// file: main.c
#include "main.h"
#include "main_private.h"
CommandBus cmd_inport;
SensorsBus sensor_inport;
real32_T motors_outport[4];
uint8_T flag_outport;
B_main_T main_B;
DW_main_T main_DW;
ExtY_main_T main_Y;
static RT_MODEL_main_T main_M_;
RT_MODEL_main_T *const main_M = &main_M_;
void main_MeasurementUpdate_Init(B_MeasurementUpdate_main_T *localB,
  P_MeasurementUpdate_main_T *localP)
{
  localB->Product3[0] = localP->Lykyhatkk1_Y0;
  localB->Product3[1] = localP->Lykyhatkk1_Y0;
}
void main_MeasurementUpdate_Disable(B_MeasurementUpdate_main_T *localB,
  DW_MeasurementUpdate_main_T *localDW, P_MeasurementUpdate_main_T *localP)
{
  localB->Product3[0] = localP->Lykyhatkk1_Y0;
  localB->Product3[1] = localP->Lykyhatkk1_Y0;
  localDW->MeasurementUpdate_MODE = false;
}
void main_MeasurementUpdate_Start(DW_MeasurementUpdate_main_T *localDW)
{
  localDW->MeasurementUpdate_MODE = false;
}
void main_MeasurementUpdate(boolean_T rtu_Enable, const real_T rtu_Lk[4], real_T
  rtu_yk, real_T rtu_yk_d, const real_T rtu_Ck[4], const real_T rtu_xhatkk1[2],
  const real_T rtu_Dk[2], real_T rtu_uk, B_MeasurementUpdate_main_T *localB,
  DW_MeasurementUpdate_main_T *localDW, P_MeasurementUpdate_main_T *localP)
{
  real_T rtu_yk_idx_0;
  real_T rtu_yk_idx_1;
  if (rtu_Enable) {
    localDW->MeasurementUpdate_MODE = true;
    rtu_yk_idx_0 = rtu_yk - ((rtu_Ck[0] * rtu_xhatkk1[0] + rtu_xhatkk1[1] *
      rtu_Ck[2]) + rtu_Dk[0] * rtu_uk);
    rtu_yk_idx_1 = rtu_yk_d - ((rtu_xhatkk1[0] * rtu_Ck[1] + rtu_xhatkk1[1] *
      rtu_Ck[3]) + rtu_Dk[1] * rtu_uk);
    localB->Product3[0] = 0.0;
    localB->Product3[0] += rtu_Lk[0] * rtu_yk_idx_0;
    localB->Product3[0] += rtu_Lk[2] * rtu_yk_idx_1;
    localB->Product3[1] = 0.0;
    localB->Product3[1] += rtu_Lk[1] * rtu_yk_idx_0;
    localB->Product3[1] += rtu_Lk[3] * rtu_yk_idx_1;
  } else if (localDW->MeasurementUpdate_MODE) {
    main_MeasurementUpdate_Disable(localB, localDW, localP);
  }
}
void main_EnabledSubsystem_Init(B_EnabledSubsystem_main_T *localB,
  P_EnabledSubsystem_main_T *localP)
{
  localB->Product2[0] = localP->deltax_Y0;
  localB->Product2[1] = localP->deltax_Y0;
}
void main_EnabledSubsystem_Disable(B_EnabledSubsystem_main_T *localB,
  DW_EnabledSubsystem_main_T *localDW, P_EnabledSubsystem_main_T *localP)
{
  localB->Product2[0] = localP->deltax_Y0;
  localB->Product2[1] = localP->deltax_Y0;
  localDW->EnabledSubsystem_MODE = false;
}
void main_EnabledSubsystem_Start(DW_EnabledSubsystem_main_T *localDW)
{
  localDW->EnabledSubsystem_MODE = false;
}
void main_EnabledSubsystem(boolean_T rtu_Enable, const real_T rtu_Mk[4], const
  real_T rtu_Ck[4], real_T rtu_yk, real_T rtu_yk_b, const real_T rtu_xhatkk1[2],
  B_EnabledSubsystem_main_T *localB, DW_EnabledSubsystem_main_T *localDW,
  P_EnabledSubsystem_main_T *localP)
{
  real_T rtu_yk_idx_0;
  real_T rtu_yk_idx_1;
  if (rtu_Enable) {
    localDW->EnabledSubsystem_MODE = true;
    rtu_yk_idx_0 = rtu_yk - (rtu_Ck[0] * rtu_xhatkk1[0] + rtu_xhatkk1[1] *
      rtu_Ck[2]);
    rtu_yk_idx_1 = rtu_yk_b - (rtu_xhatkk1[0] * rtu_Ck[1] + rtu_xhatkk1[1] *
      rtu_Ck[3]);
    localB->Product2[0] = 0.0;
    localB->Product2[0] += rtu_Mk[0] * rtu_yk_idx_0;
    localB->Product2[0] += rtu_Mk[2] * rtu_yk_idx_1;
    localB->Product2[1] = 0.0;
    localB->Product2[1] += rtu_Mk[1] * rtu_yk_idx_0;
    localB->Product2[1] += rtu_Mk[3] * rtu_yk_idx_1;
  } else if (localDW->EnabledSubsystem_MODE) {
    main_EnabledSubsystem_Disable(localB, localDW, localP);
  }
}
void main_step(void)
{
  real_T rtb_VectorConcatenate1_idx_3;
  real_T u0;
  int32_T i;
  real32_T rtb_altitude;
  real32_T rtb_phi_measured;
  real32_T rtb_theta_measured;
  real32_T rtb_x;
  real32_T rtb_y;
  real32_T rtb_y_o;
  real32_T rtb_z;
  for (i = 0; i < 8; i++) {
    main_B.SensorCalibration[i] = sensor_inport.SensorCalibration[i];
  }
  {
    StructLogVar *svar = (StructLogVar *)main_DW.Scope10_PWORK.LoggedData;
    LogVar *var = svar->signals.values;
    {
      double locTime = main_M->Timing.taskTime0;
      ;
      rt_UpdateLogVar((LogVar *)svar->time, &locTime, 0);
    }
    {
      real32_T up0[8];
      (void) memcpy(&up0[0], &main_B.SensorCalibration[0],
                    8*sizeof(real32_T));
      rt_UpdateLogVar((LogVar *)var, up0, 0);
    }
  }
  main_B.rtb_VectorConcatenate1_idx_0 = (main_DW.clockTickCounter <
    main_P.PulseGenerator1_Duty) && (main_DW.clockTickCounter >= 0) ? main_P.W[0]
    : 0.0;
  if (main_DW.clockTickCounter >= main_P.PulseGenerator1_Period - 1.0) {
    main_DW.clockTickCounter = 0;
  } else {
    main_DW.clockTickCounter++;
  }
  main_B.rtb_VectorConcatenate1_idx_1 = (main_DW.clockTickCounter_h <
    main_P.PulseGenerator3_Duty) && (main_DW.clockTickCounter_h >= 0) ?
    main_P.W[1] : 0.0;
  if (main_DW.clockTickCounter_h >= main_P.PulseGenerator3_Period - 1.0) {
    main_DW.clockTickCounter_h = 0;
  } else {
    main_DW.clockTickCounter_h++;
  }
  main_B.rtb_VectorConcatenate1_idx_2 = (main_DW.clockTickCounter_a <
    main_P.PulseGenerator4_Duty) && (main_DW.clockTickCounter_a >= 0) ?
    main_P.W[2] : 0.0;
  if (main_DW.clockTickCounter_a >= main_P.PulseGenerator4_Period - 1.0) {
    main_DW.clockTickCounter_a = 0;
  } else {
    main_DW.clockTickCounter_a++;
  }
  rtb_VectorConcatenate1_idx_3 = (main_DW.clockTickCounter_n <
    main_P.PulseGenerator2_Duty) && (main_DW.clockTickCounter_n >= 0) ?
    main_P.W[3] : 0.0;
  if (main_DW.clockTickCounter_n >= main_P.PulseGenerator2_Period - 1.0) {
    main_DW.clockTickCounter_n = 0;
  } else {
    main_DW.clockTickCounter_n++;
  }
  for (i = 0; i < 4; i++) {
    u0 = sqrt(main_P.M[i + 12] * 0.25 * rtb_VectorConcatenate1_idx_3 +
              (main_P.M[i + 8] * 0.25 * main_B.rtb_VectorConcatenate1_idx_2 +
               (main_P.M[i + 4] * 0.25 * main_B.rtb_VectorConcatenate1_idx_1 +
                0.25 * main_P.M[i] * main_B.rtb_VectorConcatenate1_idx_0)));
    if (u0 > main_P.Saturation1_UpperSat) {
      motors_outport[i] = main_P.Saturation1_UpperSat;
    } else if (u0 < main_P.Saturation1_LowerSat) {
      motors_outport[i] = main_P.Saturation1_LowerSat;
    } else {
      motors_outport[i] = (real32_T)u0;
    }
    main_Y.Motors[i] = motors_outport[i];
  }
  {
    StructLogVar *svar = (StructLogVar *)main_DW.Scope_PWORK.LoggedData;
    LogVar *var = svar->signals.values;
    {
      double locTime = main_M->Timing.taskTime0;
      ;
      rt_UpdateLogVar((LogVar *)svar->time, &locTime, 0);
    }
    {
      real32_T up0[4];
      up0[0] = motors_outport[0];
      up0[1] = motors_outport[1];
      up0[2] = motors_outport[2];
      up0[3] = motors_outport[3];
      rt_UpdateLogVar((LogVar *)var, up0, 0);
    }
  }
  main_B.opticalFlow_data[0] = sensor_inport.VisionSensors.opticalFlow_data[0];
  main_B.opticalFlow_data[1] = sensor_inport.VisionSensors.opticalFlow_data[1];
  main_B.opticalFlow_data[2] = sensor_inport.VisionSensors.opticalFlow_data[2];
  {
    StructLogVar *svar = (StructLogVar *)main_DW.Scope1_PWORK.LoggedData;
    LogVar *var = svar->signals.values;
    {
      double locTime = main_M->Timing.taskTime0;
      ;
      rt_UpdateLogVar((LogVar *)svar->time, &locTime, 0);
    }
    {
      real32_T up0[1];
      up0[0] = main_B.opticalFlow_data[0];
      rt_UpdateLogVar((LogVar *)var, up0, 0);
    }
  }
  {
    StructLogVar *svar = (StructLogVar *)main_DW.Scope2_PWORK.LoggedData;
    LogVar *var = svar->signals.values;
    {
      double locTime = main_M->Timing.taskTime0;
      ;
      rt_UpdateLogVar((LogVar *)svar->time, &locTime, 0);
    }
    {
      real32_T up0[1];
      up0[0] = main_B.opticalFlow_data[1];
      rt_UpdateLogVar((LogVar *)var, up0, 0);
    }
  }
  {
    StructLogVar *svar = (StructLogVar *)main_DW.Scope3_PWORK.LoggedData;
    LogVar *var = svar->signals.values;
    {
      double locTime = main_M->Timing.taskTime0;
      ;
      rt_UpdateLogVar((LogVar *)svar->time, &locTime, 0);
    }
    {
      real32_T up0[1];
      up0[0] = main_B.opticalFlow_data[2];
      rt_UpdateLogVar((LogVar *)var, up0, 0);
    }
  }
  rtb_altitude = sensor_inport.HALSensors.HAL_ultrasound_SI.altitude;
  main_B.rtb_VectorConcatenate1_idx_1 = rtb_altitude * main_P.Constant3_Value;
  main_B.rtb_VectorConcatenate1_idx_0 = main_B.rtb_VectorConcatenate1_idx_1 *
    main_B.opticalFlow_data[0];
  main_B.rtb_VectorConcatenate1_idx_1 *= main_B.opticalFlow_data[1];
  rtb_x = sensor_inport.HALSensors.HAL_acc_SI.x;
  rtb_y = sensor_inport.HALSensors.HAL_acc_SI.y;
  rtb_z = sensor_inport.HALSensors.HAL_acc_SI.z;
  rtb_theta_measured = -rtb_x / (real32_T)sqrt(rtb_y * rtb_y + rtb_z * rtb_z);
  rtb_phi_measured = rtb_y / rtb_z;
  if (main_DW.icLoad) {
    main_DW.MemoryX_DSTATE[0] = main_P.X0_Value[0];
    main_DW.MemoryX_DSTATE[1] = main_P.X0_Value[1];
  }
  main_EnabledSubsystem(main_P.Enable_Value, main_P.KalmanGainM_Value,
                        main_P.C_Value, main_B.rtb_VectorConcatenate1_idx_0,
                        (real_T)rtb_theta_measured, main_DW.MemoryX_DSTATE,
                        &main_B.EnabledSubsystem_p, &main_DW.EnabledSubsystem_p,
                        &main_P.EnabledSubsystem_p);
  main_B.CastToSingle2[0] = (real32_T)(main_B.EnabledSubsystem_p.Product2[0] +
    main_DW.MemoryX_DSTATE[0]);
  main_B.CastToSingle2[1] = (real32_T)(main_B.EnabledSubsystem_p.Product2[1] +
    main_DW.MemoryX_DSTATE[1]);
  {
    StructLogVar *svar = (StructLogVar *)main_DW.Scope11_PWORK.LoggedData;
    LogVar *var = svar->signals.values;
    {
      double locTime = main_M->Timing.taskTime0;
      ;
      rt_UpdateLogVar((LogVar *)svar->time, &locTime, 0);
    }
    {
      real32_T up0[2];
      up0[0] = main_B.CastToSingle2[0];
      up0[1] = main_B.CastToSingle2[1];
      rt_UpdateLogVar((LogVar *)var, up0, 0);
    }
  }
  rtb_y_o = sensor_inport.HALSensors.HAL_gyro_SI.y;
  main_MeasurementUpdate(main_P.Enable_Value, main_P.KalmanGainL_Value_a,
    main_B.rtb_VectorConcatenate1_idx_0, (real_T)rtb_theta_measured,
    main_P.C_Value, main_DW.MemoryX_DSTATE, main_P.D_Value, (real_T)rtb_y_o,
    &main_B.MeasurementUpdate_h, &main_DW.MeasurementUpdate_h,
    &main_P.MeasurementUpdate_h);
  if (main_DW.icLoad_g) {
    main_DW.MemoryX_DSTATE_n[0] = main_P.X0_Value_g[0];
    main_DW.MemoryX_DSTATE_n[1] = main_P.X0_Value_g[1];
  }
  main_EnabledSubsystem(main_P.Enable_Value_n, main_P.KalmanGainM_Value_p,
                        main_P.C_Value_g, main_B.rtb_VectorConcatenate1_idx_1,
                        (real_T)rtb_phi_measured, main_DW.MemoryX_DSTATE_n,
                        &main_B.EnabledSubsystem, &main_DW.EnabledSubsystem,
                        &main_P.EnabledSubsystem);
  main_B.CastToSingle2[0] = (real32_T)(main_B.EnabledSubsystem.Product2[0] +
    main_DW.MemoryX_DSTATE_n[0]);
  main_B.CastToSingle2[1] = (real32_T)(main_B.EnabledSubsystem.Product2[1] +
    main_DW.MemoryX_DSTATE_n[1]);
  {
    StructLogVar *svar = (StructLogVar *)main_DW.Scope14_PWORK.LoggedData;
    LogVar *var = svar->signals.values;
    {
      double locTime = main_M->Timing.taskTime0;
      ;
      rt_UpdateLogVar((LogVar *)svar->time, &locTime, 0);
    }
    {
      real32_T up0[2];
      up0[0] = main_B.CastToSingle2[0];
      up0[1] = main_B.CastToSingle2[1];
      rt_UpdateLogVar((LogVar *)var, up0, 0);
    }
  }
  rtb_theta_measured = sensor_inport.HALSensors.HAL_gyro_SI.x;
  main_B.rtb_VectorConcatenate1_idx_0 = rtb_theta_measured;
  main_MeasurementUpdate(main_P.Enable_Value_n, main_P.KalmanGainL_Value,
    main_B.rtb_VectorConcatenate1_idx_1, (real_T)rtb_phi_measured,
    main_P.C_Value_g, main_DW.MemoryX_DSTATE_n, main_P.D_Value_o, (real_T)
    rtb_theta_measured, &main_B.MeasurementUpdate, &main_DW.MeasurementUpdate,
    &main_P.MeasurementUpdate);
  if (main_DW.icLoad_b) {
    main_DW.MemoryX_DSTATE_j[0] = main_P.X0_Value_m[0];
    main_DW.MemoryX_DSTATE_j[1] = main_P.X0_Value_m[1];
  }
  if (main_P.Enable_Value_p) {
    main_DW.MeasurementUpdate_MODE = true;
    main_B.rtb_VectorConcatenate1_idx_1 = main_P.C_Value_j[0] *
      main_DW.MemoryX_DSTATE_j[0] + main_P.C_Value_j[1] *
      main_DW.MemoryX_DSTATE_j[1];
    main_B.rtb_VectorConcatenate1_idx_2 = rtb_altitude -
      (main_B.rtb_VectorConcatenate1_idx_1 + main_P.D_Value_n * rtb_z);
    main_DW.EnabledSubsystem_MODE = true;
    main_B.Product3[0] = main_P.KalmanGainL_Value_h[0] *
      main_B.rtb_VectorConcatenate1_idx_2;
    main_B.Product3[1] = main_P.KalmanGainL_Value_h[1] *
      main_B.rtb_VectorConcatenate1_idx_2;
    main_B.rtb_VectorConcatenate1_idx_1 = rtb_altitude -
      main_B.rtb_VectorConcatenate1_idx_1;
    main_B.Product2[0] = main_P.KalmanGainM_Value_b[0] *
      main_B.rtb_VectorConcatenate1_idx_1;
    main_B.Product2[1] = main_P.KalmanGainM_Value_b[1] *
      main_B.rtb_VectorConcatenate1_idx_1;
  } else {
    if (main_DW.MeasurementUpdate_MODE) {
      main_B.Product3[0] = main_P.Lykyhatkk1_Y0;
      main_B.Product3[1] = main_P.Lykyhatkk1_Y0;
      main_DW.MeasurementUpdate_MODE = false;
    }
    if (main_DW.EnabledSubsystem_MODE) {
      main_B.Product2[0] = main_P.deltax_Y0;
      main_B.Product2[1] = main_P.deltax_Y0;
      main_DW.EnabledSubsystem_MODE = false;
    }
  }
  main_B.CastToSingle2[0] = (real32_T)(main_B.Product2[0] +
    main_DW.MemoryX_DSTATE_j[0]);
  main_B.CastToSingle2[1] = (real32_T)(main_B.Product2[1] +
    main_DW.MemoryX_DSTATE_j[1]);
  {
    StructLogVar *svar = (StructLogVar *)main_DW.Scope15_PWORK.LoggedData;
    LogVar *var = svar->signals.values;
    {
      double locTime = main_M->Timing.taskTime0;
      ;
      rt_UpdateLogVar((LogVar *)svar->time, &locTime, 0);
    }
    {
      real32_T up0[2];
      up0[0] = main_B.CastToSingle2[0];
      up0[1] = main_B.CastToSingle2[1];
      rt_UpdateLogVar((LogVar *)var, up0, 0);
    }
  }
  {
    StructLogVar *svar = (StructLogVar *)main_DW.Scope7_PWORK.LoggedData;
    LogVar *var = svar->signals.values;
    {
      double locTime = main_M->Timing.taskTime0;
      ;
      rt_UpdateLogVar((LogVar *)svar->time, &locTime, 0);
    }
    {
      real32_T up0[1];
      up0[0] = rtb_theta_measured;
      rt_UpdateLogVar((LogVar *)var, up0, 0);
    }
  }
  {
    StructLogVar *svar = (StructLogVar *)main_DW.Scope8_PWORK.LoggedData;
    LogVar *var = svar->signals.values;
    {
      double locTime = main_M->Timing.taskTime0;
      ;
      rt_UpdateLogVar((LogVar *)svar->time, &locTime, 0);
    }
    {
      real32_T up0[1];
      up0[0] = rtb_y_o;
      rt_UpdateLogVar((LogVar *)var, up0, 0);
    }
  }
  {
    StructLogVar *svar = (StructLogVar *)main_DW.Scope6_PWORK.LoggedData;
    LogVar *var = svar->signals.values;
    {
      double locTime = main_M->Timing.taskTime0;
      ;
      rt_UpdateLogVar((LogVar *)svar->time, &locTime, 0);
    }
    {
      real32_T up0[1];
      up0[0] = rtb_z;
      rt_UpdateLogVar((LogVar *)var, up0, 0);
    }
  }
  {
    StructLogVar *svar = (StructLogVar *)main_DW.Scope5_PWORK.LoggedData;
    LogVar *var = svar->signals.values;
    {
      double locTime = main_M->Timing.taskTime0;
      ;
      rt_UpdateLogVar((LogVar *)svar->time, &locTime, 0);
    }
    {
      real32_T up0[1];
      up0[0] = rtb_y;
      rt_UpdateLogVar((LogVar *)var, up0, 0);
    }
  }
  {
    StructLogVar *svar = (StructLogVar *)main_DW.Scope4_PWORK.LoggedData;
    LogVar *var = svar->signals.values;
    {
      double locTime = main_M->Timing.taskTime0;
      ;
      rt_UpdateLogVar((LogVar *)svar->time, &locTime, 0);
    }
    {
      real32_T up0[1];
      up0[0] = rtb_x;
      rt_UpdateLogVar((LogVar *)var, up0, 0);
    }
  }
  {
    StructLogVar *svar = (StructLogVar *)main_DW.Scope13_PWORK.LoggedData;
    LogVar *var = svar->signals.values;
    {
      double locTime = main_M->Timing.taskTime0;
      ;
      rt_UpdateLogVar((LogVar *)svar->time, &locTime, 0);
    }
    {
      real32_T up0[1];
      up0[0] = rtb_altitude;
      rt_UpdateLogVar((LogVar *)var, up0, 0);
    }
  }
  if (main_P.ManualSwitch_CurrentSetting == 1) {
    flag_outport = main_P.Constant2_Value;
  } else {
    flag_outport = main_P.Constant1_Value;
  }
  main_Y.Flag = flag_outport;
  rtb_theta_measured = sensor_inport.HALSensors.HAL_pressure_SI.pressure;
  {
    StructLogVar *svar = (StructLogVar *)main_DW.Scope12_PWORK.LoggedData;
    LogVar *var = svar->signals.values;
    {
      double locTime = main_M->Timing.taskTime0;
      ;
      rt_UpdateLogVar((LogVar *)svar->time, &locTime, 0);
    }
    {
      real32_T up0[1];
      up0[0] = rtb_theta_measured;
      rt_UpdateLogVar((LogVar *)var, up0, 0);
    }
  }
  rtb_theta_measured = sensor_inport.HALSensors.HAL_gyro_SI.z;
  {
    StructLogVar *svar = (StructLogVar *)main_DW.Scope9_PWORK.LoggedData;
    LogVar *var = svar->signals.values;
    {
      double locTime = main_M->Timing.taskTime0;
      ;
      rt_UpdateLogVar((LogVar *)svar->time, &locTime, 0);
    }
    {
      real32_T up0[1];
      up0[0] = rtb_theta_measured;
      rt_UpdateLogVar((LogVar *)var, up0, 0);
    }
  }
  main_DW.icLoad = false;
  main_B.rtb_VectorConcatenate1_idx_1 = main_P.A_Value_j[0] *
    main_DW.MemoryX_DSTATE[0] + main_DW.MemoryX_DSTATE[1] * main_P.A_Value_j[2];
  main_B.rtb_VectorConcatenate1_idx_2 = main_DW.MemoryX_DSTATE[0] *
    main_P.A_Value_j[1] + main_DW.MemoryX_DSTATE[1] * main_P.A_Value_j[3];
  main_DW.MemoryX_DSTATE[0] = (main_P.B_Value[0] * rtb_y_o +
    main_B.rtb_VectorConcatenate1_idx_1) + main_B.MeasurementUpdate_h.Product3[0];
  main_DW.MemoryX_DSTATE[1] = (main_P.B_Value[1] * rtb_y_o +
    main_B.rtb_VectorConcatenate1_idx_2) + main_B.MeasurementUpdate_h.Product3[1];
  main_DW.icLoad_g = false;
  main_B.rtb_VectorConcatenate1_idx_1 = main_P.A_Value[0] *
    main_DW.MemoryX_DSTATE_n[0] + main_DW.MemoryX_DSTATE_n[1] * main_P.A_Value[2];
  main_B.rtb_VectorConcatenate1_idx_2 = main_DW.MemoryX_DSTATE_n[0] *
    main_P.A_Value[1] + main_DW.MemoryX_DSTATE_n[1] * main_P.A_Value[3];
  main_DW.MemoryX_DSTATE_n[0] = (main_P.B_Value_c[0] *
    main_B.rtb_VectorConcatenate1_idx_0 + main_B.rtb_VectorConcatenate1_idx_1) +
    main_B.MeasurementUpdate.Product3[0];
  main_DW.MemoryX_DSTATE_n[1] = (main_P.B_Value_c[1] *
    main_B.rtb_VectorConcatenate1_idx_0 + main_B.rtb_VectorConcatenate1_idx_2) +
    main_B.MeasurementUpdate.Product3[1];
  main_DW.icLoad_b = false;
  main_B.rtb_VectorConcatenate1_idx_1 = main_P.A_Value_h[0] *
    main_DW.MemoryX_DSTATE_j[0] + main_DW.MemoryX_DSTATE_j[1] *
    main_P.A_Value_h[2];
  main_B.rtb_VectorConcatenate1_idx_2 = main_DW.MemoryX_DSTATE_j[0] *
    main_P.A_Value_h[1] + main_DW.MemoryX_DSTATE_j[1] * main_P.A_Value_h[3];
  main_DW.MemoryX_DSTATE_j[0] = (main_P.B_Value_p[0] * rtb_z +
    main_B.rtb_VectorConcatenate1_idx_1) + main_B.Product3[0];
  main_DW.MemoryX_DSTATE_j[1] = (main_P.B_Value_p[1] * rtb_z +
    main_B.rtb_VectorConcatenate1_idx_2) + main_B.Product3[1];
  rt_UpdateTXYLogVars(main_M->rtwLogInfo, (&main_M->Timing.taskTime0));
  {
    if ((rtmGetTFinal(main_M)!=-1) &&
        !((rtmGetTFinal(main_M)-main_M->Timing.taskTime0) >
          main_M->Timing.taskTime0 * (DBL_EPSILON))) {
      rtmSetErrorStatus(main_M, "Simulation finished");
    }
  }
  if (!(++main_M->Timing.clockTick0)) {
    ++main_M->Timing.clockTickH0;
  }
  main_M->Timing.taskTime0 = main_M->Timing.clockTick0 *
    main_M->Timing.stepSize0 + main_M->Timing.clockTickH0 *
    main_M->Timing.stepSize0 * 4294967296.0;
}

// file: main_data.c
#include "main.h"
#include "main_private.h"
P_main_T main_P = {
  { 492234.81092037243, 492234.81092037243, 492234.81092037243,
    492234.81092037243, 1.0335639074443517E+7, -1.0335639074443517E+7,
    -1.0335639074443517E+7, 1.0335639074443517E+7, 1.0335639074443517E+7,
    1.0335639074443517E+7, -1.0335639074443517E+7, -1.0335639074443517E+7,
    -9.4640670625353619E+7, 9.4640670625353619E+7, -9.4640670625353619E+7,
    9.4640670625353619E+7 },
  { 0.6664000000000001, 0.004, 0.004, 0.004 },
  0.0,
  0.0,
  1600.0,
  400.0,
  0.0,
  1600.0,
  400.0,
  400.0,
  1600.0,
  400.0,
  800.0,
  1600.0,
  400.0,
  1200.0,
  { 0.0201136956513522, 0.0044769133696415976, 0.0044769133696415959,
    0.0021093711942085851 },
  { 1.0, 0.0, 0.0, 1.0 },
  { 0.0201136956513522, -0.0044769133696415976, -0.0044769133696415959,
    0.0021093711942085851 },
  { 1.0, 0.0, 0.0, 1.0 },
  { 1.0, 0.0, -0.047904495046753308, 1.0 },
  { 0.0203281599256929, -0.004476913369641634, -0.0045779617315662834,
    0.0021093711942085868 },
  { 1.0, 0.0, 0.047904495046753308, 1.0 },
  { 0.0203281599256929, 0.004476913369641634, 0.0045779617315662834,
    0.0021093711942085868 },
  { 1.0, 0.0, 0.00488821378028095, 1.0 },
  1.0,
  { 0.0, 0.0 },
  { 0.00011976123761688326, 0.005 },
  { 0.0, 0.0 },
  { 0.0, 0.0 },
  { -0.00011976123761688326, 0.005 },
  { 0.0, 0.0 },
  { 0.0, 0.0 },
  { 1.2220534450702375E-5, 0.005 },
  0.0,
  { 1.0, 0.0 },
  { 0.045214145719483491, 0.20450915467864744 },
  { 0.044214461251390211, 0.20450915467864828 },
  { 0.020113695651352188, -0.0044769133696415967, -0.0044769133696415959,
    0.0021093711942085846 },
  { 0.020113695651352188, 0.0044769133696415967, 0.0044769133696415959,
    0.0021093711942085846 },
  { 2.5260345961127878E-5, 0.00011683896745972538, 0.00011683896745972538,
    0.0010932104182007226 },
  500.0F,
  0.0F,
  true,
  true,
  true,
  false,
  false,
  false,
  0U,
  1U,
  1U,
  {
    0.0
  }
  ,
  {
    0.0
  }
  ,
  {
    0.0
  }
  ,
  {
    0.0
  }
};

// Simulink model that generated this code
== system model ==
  Inport#1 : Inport
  Inport#2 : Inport
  Motors : Outport  <- 1: Saturation1
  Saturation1 : Saturate  UpperLimit=500  LowerLimit=0  <- 1: Sqrt#1
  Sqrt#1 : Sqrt  <- 1: Gain#1
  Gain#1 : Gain  Gain=1/4*M  Multiplication=Matrix(K*u)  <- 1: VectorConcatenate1
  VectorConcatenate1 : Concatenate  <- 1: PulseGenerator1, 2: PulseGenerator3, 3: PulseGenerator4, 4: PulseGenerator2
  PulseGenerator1 : DiscretePulseGenerator  Amplitude=W(1)  Period=1600  PulseWidth=400
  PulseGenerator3 : DiscretePulseGenerator  Amplitude=W(2)  Period=1600  PulseWidth=400  PhaseDelay=400
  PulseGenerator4 : DiscretePulseGenerator  Amplitude=W(3)  Period=1600  PulseWidth=400  PhaseDelay=800
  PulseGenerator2 : DiscretePulseGenerator  Amplitude=W(4)  Period=1600  PulseWidth=400  PhaseDelay=1200
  Flag : Outport  <- 1: ManualSwitch
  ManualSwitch : ManualSwitch  <- 1: Constant2, 2: Constant1
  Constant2 : Constant  Value=0
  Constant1 : Constant
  DataTypeConversion#1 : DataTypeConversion  <- 1: KalmanFilter#1
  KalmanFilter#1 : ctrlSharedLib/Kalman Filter  TimeDomain=Discrete-Time  A=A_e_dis  B=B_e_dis  C=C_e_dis  D=[0]  X0=0  N=0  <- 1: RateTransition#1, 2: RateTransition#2
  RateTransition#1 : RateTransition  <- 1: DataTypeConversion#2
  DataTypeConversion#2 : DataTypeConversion  <- 1: BusSelector#1/2
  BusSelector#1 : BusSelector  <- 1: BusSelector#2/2
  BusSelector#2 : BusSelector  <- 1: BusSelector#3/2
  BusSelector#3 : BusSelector  <- 1: Inport#2
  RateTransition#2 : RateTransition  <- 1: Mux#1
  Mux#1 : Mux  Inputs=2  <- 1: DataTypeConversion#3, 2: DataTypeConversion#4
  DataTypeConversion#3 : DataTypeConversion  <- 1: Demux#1
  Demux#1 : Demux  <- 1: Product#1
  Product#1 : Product  <- 1: Product#2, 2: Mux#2
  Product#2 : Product  <- 1: BusSelector#4, 2: Constant3
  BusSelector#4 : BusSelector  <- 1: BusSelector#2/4
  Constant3 : Constant
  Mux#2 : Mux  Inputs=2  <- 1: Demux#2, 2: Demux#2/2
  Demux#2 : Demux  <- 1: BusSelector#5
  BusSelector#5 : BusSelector  <- 1: BusSelector#3
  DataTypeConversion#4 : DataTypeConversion  <- 1: MATLABFunction#1
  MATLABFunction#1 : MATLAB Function  <- 1: BusSelector#6, 2: BusSelector#6/2, 3: BusSelector#6/3
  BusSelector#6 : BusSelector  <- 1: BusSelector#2
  DataTypeConversion#5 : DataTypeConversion  <- 1: KalmanFilter#2
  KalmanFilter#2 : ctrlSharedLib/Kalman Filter  TimeDomain=Discrete-Time  A=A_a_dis  B=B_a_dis  C=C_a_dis  D=[0;0]  X0=[0;0]  N=0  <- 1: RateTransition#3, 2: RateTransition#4
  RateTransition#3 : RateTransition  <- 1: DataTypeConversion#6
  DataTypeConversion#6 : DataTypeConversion  <- 1: BusSelector#1
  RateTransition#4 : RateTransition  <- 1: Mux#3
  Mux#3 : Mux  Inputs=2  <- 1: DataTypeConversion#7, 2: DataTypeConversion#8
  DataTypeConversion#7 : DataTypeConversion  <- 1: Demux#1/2
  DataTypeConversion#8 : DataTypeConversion  <- 1: MATLABFunction#1/2
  CastToSingle2 : DataTypeConversion  <- 1: KalmanFilter#3
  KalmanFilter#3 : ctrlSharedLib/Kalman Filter  TimeDomain=Discrete-Time  A=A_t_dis  B=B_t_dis  C=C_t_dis  D=0  X0=0  N=0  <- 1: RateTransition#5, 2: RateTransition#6
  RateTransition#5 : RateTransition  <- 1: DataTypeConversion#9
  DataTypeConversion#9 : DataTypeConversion  <- 1: BusSelector#6/3
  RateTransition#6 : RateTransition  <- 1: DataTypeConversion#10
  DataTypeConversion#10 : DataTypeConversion  <- 1: BusSelector#4
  BusSelector#7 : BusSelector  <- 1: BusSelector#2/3
== matlab function MATLABFunction#1 ==
function [theta_measured,phi_measured]= fcn(a_x,a_y,a_z)
theta_measured = -a_x / sqrt(a_y^2 + a_z^2);
phi_measured = a_y/a_z;
